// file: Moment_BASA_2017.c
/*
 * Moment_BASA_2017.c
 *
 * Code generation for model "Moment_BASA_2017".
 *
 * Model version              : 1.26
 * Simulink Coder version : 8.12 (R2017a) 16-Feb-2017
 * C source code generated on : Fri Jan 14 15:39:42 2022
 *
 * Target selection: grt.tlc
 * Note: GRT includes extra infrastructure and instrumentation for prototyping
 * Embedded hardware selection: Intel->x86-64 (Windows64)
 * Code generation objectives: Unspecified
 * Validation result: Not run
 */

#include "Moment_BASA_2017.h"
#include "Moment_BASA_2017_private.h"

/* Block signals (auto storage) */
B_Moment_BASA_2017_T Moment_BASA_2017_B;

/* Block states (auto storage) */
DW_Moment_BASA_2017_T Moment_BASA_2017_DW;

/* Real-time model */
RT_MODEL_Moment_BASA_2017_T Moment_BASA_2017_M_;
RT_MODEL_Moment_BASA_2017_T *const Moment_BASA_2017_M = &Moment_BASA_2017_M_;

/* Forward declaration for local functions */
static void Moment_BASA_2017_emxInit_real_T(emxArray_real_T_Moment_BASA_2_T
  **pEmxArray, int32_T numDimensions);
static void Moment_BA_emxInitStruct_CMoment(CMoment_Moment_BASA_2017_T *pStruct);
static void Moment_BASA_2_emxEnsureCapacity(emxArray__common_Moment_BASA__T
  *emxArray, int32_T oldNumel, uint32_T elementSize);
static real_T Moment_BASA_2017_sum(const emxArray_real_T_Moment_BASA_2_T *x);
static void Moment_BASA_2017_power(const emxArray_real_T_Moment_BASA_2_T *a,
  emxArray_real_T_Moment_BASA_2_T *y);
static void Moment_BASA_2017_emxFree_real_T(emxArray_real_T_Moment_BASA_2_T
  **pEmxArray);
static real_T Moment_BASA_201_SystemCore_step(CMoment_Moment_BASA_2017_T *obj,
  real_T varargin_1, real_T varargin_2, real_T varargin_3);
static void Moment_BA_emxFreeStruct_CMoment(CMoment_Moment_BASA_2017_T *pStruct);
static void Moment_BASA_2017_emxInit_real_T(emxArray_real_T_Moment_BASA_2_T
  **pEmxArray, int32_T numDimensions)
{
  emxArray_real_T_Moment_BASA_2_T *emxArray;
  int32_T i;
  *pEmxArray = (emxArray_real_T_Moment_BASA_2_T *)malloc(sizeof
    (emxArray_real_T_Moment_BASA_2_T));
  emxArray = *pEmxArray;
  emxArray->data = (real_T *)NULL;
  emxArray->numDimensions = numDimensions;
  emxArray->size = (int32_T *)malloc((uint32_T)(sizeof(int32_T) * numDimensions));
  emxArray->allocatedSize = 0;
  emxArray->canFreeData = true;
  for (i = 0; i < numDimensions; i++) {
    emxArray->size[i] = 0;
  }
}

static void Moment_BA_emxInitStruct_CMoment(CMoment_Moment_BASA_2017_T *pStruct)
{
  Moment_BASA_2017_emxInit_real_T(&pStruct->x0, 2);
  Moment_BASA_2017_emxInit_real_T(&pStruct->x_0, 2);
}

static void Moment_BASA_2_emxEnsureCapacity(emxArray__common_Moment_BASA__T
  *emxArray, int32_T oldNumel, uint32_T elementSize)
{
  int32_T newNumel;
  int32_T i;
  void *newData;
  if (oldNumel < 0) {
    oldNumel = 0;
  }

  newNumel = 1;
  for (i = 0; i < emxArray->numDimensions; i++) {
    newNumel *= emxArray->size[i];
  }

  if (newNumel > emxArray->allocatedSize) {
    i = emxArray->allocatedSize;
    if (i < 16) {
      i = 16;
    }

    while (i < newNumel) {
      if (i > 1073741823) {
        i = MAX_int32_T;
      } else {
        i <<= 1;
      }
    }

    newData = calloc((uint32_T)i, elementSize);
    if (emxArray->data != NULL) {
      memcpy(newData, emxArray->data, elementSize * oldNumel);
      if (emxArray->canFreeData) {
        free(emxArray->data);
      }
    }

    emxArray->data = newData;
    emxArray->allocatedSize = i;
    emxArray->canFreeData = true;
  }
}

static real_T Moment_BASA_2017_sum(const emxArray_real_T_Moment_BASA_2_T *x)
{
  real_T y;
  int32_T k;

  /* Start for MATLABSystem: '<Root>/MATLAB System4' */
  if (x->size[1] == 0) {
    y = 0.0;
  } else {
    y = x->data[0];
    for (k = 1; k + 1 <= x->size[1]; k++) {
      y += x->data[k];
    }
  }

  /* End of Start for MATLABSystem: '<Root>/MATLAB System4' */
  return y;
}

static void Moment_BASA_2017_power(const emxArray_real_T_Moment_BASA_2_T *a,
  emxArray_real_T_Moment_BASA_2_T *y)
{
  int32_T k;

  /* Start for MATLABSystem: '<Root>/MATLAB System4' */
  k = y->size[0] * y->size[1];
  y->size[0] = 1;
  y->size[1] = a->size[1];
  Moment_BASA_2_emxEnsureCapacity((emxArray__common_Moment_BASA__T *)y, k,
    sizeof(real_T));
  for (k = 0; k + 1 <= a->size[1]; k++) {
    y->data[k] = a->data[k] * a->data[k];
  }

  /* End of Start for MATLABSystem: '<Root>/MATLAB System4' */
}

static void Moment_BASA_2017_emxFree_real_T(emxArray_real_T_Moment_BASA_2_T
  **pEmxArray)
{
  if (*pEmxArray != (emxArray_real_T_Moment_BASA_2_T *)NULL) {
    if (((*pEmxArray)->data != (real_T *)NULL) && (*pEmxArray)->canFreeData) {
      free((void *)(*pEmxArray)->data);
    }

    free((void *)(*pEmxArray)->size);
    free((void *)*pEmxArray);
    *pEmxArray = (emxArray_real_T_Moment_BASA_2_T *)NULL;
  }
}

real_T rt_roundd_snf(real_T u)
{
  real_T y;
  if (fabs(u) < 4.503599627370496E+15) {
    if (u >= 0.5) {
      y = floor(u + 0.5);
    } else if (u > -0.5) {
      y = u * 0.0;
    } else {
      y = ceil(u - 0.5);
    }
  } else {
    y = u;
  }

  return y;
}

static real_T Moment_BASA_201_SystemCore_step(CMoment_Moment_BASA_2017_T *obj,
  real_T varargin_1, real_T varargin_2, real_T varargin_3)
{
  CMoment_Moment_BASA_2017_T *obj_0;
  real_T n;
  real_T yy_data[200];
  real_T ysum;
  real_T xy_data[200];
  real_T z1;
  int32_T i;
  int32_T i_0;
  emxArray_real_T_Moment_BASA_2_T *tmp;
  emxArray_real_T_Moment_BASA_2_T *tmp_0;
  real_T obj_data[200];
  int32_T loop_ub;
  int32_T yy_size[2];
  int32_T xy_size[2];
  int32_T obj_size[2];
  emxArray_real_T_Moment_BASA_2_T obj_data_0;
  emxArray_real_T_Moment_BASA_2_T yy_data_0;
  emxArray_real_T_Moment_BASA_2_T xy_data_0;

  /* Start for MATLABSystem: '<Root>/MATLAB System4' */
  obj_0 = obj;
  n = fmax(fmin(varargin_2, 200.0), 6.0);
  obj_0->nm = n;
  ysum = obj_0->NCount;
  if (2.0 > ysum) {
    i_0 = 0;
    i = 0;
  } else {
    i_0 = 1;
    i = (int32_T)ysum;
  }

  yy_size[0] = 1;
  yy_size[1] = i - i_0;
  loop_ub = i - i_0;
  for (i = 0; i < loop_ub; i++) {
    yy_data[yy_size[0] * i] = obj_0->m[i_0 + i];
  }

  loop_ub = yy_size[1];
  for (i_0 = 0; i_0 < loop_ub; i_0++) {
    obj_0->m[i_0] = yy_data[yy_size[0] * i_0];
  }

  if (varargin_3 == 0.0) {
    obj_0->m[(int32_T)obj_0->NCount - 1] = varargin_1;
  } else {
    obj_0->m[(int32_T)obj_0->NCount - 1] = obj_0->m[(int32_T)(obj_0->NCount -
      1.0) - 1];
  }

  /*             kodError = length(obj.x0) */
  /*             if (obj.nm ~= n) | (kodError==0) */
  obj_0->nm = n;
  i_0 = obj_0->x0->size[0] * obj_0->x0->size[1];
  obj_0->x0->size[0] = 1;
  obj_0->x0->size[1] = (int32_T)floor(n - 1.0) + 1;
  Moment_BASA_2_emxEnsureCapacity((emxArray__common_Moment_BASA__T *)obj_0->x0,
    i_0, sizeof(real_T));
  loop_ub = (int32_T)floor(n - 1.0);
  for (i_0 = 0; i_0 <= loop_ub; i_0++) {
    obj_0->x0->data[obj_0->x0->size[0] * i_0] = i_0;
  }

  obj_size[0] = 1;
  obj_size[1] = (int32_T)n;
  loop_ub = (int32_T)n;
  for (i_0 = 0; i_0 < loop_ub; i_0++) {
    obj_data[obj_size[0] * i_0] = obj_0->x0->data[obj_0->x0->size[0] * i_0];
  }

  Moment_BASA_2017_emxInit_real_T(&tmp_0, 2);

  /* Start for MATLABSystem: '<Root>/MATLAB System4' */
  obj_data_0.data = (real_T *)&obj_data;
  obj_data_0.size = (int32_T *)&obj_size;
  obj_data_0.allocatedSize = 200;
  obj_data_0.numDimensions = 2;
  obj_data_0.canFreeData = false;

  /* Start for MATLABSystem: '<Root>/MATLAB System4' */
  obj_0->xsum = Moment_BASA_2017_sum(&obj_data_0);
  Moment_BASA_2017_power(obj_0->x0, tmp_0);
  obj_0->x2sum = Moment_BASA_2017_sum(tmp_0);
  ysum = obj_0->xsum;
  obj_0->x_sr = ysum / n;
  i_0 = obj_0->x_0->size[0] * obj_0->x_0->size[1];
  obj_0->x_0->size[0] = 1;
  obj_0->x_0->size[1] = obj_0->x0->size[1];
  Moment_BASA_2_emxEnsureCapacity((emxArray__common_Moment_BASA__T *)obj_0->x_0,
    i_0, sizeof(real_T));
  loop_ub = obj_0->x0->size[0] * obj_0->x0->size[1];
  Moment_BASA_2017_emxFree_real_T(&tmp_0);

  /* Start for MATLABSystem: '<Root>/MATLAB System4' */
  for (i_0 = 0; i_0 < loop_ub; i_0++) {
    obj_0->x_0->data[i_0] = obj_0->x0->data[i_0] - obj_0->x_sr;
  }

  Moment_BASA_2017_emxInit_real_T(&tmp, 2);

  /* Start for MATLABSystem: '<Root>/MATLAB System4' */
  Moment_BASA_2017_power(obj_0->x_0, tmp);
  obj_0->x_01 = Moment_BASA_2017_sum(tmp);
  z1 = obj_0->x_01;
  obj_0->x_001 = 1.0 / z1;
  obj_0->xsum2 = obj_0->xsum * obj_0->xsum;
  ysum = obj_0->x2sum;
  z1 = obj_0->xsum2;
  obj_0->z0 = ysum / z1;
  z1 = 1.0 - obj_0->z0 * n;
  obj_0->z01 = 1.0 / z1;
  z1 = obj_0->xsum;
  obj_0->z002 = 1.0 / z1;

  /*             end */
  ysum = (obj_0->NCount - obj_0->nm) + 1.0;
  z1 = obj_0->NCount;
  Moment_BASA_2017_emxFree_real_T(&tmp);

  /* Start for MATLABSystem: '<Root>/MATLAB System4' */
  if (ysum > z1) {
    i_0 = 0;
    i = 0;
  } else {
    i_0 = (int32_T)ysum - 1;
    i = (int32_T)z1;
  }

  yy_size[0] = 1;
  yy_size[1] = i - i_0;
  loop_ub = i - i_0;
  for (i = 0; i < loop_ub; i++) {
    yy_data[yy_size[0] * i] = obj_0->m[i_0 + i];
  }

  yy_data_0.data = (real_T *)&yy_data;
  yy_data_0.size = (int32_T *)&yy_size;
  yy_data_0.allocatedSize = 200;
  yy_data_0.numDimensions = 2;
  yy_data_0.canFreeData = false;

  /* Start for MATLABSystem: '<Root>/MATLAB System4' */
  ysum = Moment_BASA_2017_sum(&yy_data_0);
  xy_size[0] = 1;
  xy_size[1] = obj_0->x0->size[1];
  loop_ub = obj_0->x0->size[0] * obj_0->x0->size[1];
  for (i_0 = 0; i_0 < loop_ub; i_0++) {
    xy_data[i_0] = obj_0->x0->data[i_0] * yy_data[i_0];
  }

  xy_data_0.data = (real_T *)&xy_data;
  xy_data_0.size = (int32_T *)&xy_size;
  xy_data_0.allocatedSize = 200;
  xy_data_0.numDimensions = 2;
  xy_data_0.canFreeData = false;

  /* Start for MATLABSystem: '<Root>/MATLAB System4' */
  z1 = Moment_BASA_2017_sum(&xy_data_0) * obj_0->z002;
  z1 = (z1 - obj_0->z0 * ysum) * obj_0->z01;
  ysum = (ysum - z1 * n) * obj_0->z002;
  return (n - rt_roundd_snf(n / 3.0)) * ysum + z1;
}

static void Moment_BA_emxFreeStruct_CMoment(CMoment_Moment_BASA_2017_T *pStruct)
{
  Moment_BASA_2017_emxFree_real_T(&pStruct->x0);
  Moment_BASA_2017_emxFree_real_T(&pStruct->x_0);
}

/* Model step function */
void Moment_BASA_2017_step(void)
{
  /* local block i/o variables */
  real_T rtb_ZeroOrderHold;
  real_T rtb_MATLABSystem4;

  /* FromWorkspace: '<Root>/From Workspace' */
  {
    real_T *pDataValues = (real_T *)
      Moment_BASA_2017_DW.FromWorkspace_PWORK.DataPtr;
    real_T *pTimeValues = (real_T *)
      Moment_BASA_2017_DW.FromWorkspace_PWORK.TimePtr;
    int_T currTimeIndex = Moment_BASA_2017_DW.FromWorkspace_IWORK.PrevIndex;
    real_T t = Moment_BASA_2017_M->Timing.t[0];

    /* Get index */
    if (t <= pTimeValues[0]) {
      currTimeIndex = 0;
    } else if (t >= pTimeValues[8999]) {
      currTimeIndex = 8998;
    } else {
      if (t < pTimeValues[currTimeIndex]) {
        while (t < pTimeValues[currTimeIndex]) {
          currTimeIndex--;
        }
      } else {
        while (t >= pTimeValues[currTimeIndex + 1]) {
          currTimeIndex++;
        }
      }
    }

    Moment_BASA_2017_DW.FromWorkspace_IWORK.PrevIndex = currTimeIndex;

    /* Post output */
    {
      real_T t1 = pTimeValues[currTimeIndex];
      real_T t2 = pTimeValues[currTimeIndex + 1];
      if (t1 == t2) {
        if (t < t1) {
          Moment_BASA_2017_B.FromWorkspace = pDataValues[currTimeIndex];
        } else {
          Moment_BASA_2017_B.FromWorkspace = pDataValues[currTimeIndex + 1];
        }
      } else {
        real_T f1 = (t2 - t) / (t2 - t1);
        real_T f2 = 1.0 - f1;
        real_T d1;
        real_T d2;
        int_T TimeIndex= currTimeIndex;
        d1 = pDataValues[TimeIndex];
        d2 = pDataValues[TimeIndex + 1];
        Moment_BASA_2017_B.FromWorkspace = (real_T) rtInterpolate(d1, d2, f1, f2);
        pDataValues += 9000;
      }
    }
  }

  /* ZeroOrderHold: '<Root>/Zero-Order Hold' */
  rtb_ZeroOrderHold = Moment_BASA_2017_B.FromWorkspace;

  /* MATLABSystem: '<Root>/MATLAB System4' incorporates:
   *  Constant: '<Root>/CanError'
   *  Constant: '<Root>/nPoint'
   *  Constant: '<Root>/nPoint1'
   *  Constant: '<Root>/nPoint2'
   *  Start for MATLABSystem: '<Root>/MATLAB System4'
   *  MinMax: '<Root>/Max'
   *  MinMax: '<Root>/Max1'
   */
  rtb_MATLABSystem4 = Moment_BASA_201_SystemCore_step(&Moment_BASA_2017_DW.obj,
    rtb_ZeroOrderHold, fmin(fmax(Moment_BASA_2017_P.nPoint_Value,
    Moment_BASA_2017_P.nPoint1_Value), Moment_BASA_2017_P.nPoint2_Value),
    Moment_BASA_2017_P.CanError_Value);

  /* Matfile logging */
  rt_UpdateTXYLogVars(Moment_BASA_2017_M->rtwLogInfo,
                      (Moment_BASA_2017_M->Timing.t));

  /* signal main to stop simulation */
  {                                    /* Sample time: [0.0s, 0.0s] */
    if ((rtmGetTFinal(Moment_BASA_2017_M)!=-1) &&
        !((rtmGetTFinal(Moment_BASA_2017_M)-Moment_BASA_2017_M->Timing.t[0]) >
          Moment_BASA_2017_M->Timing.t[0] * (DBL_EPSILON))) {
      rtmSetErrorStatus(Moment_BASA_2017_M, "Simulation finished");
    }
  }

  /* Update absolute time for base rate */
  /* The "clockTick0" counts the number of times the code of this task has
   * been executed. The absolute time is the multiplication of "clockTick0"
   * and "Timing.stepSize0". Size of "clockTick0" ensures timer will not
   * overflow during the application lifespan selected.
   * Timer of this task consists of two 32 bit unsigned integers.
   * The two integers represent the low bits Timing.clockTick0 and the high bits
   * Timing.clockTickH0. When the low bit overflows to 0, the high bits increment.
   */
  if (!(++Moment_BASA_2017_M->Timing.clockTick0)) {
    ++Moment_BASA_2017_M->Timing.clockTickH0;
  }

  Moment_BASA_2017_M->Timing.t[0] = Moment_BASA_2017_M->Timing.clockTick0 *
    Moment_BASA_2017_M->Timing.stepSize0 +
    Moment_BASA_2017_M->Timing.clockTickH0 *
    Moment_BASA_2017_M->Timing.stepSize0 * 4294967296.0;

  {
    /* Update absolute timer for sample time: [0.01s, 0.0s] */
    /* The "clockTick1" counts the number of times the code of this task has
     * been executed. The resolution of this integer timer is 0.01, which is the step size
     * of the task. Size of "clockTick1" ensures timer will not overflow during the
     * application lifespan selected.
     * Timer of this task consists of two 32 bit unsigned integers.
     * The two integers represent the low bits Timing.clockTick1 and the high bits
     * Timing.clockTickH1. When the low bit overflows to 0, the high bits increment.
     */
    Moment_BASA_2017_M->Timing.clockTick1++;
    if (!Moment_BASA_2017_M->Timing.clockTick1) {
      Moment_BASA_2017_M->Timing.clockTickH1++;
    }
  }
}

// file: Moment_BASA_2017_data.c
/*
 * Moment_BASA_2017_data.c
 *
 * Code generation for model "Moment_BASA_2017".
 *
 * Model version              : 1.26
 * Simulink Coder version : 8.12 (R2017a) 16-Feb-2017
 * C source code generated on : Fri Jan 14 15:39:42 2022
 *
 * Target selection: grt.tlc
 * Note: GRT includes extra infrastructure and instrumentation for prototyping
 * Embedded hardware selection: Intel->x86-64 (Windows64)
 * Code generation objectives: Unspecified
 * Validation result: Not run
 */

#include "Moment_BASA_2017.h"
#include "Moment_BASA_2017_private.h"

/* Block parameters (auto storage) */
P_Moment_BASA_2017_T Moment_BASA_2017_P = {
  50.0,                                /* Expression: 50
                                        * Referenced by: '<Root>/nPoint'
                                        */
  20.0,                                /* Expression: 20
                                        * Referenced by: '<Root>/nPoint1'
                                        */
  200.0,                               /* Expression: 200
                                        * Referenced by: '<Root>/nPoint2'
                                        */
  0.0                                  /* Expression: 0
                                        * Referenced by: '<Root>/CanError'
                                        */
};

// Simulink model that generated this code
simulink model "Moment_BASA_2017"  (R2017a)
settings: Solver=FixedStepAuto  StartTime=0  StopTime=9000  FixedStep=0.01  RelTol=1e-3

== system Moment_BASA_2017 ==
  CanError : Constant  Value=0
  From Workspace : FromWorkspace  VariableName=tMoment  SampleTime=0
  MATLAB System4 : MATLABSystem  System=CMoment  SimulateUsing=Code generation
  Max : MinMax  Function=max  Inputs=2
  Max1 : MinMax  Inputs=2
  Scope : Scope  NumInputPorts=2
  Zero-Order Hold : ZeroOrderHold  SampleTime=0.01
  nPoint : Constant  Value=50
  nPoint1 : Constant  Value=20
  nPoint2 : Constant  Value=200
  wires:
  CanError/1 -> MATLAB System4/3
  From Workspace/1 -> Zero-Order Hold/1
  Zero-Order Hold/1 -> MATLAB System4/1, Scope/1
  nPoint/1 -> Max/1
  nPoint1/1 -> Max/2
  Max/1 -> Max1/1
  nPoint2/1 -> Max1/2
  Max1/1 -> MATLAB System4/2
  MATLAB System4/1 -> Scope/2
